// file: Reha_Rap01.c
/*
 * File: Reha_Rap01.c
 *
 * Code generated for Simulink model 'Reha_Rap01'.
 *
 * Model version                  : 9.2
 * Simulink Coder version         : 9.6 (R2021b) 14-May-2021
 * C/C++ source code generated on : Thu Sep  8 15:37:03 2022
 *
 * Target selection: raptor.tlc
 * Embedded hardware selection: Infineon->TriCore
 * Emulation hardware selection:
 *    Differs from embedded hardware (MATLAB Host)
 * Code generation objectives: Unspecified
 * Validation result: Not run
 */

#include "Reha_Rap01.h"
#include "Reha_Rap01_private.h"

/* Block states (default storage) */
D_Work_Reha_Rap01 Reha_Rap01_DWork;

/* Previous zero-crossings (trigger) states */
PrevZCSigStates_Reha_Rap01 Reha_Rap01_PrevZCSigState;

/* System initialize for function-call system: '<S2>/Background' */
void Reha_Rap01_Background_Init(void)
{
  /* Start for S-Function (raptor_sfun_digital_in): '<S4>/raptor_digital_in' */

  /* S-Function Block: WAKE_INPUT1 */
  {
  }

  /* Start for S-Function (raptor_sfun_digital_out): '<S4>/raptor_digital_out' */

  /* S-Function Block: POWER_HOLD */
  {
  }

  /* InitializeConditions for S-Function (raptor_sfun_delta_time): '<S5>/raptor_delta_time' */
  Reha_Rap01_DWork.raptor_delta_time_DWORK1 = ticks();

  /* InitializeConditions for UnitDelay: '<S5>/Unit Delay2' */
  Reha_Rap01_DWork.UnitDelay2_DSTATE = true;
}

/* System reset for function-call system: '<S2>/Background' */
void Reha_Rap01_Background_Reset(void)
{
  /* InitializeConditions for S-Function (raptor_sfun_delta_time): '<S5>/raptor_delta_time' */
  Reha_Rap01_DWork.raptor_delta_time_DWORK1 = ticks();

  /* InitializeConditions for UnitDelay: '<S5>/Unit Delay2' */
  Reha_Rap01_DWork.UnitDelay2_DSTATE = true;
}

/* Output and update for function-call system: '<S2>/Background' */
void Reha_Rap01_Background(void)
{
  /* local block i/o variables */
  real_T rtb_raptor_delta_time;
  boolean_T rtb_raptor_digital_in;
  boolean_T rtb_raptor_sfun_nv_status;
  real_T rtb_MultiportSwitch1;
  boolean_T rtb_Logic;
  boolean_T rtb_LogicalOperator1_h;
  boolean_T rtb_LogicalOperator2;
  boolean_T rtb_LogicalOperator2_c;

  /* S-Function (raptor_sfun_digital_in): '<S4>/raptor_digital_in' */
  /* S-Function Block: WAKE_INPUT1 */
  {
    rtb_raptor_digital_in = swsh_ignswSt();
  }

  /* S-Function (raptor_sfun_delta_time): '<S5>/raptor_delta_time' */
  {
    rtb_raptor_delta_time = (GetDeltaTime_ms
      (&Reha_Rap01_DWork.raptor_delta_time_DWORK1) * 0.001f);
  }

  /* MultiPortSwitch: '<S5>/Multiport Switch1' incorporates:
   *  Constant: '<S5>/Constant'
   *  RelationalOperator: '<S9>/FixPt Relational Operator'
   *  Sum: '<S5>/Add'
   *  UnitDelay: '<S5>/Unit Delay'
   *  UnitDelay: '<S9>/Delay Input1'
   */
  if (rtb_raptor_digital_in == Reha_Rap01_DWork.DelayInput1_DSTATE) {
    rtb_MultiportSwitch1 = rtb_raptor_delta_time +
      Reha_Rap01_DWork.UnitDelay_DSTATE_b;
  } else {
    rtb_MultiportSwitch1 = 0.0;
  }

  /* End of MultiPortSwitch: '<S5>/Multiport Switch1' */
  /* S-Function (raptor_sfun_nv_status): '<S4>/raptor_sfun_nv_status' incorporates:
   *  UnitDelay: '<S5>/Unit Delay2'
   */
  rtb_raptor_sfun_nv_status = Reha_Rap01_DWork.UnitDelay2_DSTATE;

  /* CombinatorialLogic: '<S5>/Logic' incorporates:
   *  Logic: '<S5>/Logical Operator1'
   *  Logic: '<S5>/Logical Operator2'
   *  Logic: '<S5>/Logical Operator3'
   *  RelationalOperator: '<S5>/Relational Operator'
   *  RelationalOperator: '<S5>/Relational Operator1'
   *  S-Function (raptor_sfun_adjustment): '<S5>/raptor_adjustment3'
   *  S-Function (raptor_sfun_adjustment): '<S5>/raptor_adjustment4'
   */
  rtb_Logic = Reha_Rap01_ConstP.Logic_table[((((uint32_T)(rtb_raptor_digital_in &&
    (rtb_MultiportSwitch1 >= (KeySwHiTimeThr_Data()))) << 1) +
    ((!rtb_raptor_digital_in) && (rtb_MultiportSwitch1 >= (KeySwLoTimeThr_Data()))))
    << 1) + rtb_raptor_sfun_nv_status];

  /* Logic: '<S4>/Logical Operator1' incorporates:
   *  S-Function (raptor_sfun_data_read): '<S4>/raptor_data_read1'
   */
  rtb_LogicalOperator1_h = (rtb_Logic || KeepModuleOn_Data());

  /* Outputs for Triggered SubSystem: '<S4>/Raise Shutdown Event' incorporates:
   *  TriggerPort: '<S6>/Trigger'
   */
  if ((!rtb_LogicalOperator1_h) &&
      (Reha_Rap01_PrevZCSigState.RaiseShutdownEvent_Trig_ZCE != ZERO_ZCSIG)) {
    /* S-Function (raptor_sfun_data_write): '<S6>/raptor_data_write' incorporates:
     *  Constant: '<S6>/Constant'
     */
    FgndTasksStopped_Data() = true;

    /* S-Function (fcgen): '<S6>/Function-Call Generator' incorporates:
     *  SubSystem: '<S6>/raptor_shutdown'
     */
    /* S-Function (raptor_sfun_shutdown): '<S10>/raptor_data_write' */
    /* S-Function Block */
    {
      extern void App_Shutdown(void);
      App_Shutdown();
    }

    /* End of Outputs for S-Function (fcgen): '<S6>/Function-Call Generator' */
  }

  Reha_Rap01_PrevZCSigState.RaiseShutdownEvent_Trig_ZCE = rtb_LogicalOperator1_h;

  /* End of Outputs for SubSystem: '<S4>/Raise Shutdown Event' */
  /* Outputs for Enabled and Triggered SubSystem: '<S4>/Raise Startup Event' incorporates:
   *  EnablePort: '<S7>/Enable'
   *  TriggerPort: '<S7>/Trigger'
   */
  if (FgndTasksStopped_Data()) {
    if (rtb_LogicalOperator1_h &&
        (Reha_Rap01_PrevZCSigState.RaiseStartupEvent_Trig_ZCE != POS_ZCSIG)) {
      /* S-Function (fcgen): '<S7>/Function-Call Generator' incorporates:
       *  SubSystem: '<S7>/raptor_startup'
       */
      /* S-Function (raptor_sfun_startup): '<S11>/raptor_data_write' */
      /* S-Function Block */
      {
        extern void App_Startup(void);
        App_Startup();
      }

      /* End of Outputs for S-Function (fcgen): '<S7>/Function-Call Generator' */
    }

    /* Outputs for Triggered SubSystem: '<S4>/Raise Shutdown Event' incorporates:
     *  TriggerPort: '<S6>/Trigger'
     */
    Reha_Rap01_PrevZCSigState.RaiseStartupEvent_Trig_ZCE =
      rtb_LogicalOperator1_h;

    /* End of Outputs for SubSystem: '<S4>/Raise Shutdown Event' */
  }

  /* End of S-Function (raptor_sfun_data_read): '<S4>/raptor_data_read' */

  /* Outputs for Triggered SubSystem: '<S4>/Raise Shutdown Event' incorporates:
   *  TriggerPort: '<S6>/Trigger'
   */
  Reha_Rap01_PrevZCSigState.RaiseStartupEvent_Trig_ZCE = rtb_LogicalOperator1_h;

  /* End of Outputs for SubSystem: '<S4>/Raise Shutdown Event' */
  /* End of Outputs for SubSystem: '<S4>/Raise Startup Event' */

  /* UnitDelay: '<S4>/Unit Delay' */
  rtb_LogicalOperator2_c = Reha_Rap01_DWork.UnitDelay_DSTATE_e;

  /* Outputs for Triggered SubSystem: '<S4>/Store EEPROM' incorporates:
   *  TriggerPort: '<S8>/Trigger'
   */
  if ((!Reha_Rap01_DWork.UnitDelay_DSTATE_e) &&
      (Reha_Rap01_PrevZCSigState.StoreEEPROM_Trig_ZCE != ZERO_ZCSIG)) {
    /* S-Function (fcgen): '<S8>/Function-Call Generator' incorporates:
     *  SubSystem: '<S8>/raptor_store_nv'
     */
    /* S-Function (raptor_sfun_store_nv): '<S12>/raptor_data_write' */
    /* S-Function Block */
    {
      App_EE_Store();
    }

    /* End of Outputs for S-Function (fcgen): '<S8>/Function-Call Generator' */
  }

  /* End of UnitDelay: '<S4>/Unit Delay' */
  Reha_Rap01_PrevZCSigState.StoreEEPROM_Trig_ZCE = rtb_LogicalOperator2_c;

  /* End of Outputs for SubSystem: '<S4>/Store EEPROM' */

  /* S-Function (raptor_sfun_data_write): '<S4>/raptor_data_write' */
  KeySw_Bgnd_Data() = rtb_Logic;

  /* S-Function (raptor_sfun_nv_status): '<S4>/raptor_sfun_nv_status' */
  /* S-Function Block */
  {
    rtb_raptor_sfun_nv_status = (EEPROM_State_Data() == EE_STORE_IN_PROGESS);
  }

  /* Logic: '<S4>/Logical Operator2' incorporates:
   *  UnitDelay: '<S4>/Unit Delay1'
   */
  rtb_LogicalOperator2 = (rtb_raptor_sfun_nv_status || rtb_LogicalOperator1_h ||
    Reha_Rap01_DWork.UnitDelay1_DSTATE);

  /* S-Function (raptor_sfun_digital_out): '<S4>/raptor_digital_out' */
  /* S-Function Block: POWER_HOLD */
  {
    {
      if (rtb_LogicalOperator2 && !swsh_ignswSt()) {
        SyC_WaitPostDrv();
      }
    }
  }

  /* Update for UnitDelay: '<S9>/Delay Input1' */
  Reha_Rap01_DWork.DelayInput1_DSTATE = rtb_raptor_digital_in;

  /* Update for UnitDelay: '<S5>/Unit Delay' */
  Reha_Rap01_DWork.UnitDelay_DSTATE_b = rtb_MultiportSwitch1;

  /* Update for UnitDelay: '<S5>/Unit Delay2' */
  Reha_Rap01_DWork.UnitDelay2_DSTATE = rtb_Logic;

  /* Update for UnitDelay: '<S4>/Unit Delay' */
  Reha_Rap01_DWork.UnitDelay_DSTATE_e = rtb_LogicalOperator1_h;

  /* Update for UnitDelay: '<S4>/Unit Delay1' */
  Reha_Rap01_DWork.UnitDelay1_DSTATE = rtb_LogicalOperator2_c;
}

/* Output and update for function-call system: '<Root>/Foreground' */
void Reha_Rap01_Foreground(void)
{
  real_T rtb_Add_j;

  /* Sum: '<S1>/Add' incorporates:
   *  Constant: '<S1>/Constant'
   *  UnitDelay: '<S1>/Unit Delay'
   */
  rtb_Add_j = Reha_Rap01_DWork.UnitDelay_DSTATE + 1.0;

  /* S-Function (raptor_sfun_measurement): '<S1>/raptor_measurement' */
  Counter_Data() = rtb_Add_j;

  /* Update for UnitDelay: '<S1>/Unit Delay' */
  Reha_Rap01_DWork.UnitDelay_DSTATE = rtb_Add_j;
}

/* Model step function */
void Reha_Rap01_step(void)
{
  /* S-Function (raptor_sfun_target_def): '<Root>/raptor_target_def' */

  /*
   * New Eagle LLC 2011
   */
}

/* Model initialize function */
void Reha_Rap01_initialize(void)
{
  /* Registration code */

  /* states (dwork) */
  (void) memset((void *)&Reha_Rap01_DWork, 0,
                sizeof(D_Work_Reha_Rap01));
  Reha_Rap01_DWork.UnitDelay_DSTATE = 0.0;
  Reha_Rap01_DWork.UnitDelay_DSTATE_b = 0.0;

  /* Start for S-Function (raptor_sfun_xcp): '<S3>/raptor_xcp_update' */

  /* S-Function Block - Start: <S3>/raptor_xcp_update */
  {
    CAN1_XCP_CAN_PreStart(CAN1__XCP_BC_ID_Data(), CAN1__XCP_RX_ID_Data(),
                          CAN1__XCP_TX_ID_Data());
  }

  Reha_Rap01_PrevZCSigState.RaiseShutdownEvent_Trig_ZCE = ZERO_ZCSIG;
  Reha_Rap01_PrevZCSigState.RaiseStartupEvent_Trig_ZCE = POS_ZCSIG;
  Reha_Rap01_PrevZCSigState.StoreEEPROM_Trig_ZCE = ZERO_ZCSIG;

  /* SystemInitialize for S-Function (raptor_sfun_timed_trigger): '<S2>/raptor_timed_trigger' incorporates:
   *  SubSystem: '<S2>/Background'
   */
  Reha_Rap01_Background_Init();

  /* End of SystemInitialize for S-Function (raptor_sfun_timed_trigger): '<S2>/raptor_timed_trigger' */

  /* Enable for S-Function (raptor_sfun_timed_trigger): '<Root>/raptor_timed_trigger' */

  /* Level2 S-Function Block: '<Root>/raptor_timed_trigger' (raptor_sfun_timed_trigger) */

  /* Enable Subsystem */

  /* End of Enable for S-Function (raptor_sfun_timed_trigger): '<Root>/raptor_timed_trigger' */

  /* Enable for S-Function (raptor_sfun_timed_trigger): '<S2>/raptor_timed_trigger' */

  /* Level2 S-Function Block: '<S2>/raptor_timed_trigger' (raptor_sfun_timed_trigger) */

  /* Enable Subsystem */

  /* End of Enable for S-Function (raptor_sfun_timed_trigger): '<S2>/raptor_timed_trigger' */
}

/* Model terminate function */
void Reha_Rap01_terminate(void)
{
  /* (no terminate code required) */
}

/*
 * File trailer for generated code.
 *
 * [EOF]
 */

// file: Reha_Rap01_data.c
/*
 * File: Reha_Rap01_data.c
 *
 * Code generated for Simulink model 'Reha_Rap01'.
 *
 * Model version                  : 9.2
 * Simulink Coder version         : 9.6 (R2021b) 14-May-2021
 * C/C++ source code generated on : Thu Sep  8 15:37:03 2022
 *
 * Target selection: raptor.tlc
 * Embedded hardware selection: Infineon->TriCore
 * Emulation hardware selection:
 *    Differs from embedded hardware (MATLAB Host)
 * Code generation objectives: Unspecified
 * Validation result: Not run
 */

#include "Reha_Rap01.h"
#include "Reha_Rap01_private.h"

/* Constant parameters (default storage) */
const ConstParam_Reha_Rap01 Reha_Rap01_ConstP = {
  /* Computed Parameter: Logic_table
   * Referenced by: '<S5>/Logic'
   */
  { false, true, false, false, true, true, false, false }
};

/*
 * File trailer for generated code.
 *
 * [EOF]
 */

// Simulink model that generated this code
simulink model "Reha_Rap01"  (R2021b)
settings: Solver=FixedStepDiscrete  StartTime=0.0  StopTime=10.0  FixedStep=0.005  RelTol=1e-3  EnableMultiTasking=on
PreLoadFcn:
  | try, model_open; catch, disp('Error occurred while executing model pre-load callback: model_open.m'); disp('Please assure that the MATLAB working directory is set to the model directory before opening.'); end
InitFcn:
  | try, model_open; catch, end
undefined symbols (not defined in the file): ECM, raptor_get_safe_string, raptor_xcp_function
libraries: Raptor_lib x22, simulink x4

== system Reha_Rap01 ==
  Foreground : Subsystem  TreatAsAtomicUnit=on
  Power Up_Down : Subsystem  mask{group='Diagnostics | Power Up_Down'}
  raptor_can_def : Raptor_lib/CAN/raptor_can_def  canBus='CAN1'  resourceValues=(None)|CAN1|CAN2  resource=CAN1  baudRateValues=250k  baudRate=250k  enable_baud_rate_config='RAPTOR MASK DEFAULT'  sim_func_name='RAPTOR MASK DEFAULT'  createButton=[]  txQueueSize=16  rxQueueSize=16
  raptor_target_def : Raptor_lib/Configuration/raptor_target_def  targetValues=HCM-5534-50-1203|HCM-5534-90-1201|HCM-5534-90-1302|HCM-5604-36-1303|HCM-ARM4-070-1401|DISP-IMX286-036-1402|DISP-IMX286-024-1204|DISP-IMX286-012-1402  target=ECM-1793-196-1503  simpack=0  simulator=0  heap=4*1024  stack=2*1024  fgndStack=3*1024  bgndStack=2*1024  idleStack=1024  intStack=1536  sdStack=1024  appStack=1024  ecuaddr=11  uds_server_addr_ext=0  uds_server_addr=hex2dec('600')  uds_client_addr=hex2dec('650')  callocValues=Constant (FLASH)|NonVolatile (EEPROM)  calloc=NonVolatile (EEPROM)  compilerValues=HighTec v3.4.5.11  compiler=HighTec v3.4.5.11  setFileName=0  exeName=[raptor_get_safe_string(bdroot) '_']  addBuildNum=1  minVerChars=3  extraOutput=0  buildLocationValues=Raptor Default|Model Directory|User Defined  buildLocation=Raptor Default  exeLocation=''  exeFileButton=[]  a2lLocation=''  a2lFileButton=[]  rpgLocation=''  rpgFileButton=[]
  raptor_timed_trigger : Raptor_lib/Triggers/raptor_timed_trigger  triggerValues=[]  trigger=Foreground  inherited=0  alwaysEnabled=1  triggerPriority=0  triggerName=ooqlV
  raptor_xcp_def : Raptor_lib/Configuration/raptor_xcp_def  canBus='CAN1'  bcID=hex2dec('100')  bcID_TypeValues=Standard|Extended  bcID_Type=Standard  rxID=hex2dec('200')  rxID_TypeValues=Standard|Extended  rxID_Type=Standard  txID=hex2dec('300')  txID_TypeValues=Standard|Extended  txID_Type=Standard  daqRates=[10 100]  numODTs=20  genCANAPE=0  genVISION=0  securityValues=Standard|None|Custom User Defined|MH_SB_4  security=Standard  dllName=raptor_XCPSecurity.dll  accessValues=4|3|2|1  access=1  bcStorageValues=[]  bcStorage=Calibration  txStorageValues=[]  txStorage=Calibration  rxStorageValues=[]  rxStorage=Calibration
  wires:
  raptor_timed_trigger/1 -> Foreground/Trigger

== system Reha_Rap01/Foreground ==
  function : TriggerPort  TriggerType=function-call  VariantControl=Variant
  Add : Sum
  Constant : Constant
  Unit Delay : UnitDelay  SampleTime=-1  HasFrameUpgradeWarning=on
  raptor_measurement : Raptor_lib/Data Storage/raptor_measurement  paramName='Counter'  nameSource=Parameter  calDispType=Number  calEnum={'False', 'True'}  calGain=1.0  calOffset=0.0  calMax=inf  calMin=-inf  calFormat='-1'  calUnit=''  calHelp=''  calAccess=4  calFunction=raptor_xcp_function(gcb)  calVisible=on
  wires:
  Constant/1 -> Add/1
  Add/1 -> raptor_measurement/1, Unit Delay/1
  Unit Delay/1 -> Add/2

== system Reha_Rap01/Power Up_Down ==
  Background : Subsystem
  raptor_timed_trigger : Raptor_lib/Triggers/raptor_timed_trigger  triggerValues=Foreground|Foregroundx2|Foregroundx5|Foregroundx10|Foregroundx20|Background|Backgroundx2|Backgroundx5|Backgroundx10|Backgroundx20|Second|Minute  trigger=Background  inherited=0  alwaysEnabled=1  triggerPriority=50  triggerName=BGND_G6Wyo
  wires:
  raptor_timed_trigger/1 -> Background/Trigger

== system Reha_Rap01/Power Up_Down/Background ==
  note: Notes :
      | - Calling the shutdown task stops the foreground tasks. However, background tasks continue, so the reading of key switch must be in this subsystem to allow the module
      | to resume operation (by calling the startup task) if keyswitch is turned back on before the module actually turns off.
      | - The Startup Event is automatically called when the module is powered on after being completely off. The FgndTasksStopped data store prevents the Startup Event from being called twice in this scenario.
  f : TriggerPort  TriggerType=function-call  VariantControl=Variant  ZeroCross=off
  Debounce : Subsystem
  Logical Operator1 : Logic  Operator=OR  OutDataTypeStr=boolean
  Logical Operator2 : Logic  Operator=OR  Inputs=3  OutDataTypeStr=boolean
  Raise Shutdown Event : Subsystem  TreatAsAtomicUnit=on
  Raise Startup Event : Subsystem  TreatAsAtomicUnit=on
  Store EEPROM : Subsystem  TreatAsAtomicUnit=on
  Unit Delay : UnitDelay  SampleTime=-1  HasFrameUpgradeWarning=on
  Unit Delay1 : UnitDelay  SampleTime=-1  HasFrameUpgradeWarning=on
  raptor_data_def : Raptor_lib/Data Storage/raptor_data_def  dataName='KeySw_Bgnd'  initValue=0  dataType=boolean  storage=Volatile (RAM)  calVisible=on  calType=Measurement  calDispType=Number  calEnum={'False', 'True'}  calGain=1.0  calOffset=0  calMin=-Inf  calMax=Inf  calFormat='-1'  calUnit='Bool'  calHelp='Key switch reading from background task'  calAccess=1  calFunction=group  calDispHeaders=off  calColHeaders={'Col1' 'Col2' 'Col3'}  calRowHeaders={'Row1' 'Row2' 'Row3'}
  raptor_data_def1 : Raptor_lib/Data Storage/raptor_data_def  dataName='KeepModuleOn'  initValue=0  dataType=boolean  storage=Volatile (RAM)  calVisible=on  calType=Measurement  calDispType=Number  calEnum={'False', 'True'}  calGain=1.0  calOffset=0  calMin=-Inf  calMax=Inf  calFormat='-1'  calUnit='Bool'  calHelp='Boolean indicating module to be kept on'  calAccess=1  calFunction=group  calDispHeaders=off  calColHeaders={'Col1' 'Col2' 'Col3'}  calRowHeaders={'Row1' 'Row2' 'Row3'}
  raptor_data_read : Raptor_lib/Data Storage/raptor_data_read  dataName='FgndTasksStopped'  dataShape=Scalar  idxSource=Input  idxRow=1  idxCol=1
  raptor_data_read1 : Raptor_lib/Data Storage/raptor_data_read  dataName='KeepModuleOn'  dataShape=Scalar  idxSource=Input  idxRow=1  idxCol=1
  raptor_data_write : Raptor_lib/Data Storage/raptor_data_write  dataName='KeySw_Bgnd'  dataShape=Scalar  idxSource=Input Port  idxRow=1  idxCol=1
  raptor_digital_in : Raptor_lib/Input & Output/raptor_digital_in  resourceValues=(None)|WAKE_INPUT1|INPUT33|INPUT34|INPUT35|INPUT36|INPUT37|INPUT38|INPUT39|INPUT40  resource=WAKE_INPUT1  pullUDValues=2.9k PD  pullUD=2.9k PD  upperThres=1.980  lowerThres=1.320
  raptor_digital_out : Raptor_lib/Input & Output/raptor_digital_out  resourceValues=OUTPUT9|OUTPUT21|OUTPUT22|OUTPUT23|OUTPUT24|(None)|OUTPUT1|OUTPUT2|OUTPUT3|OUTPUT4|OUTPUT5|OUTPUT6|OUTPUT7|OUTPUT8|OUTPUT10|OUTPUT11|OUTPUT25|OUTPUT26|OUTPUT27|OUTPUT28|OUTPUT29|OUTPUT30|OUTPUT31|OUTPUT32|OUTPUT33|OUTPUT34|OUTPUT35|OUTPUT36|OUTPUT37|OUTPUT38|OUTPUT39|OUTPUT40|OUTPUT41|OUTPUT42|OUTPUT43|OUTPUT44|OUTPUT45|OUTPUT46|OUTPUT47|OUTPUT48|POWER_HOLD  resource=POWER_HOLD  driverTypeValues=(None)  driverType=(None)
  raptor_sfun_nv_status : Raptor_lib/Data Storage/raptor_sfun_nv_status  showStatus=Store In Progess
  wires:
  raptor_data_read/1 -> Raise Startup Event/Enable
  raptor_digital_in/1 -> Debounce/1(In)
  Logical Operator2/1 -> raptor_digital_out/1
  Unit Delay/1 -> Store EEPROM/Trigger, Unit Delay1/1
  Logical Operator1/1 -> Logical Operator2/2, Raise Startup Event/Trigger, Raise Shutdown Event/Trigger, Unit Delay/1
  Unit Delay1/1 -> Logical Operator2/3
  raptor_sfun_nv_status/1 -> Logical Operator2/1
  raptor_data_read1/1 -> Logical Operator1/2
  Debounce/1(Out) -> raptor_data_write/1, Logical Operator1/1

== system Reha_Rap01/Power Up_Down/Background/Debounce ==
  note: Set / Reset
  In : Inport
  Add : Sum
  Constant : Constant  Value=double(0)
  Detect Change : simulink/Logic and Bit Operations/Detect Change  vinit=0  OutDataTypeStr=boolean
  Logic : CombinatorialLogic  TruthTable=[0;1;0;0;1;1;0;0]
  Logical Operator1 : Logic  AllPortsSameDT=off  OutDataTypeStr=boolean
  Logical Operator2 : Logic  AllPortsSameDT=off  OutDataTypeStr=boolean
  Logical Operator3 : Logic  Operator=NOT  Inputs=1  AllPortsSameDT=off  OutDataTypeStr=boolean
  Multiport Switch1 : MultiPortSwitch  DataPortOrder=Zero-based contiguous  Inputs=2  zeroidx=on
  Mux1 : Mux  Inputs=3
  Relational Operator : RelationalOperator  OutDataTypeStr=boolean  RndMeth=Nearest
  Relational Operator1 : RelationalOperator  OutDataTypeStr=boolean  RndMeth=Nearest
  Unit Delay : UnitDelay  SampleTime=-1  HasFrameUpgradeWarning=on
  Unit Delay2 : UnitDelay  InitialCondition=1  SampleTime=-1  HasFrameUpgradeWarning=on
  raptor_adjustment3 : Raptor_lib/Data Storage/raptor_adjustment  paramName='KeySwHiTimeThr'  nameSource=Parameter  initValue=0.2  dataType=double  storage=Calibration  calDispType=Number  calEnum={'Active Low', 'Active High'}  calGain=1  calOffset=0  calMax=inf  calMin=-inf  calFormat='-1'  calUnit='sec'  calHelp='State high time threshold'  calAccess=1  calFunction=group  calDispHeaders=off  calColHeaders={'Col1' 'Col2' 'Col3'}  calRowHeaders={'Row1' 'Row2' 'Row3'}
  raptor_adjustment4 : Raptor_lib/Data Storage/raptor_adjustment  paramName='KeySwLoTimeThr'  nameSource=Parameter  initValue=0.2  dataType=double  storage=Calibration  calDispType=Number  calEnum={'Active Low', 'Active High'}  calGain=1  calOffset=0  calMax=inf  calMin=-inf  calFormat='-1'  calUnit='sec'  calHelp='State low time threshold'  calAccess=1  calFunction=group  calDispHeaders=off  calColHeaders={'Col1' 'Col2' 'Col3'}  calRowHeaders={'Row1' 'Row2' 'Row3'}
  raptor_delta_time : Raptor_lib/Triggers/raptor_delta_time  unit=seconds
  Out : Outport  VectorParamsAs1DForOutWhenUnconnected=off
  wires:
  Detect Change/1 -> Multiport Switch1/1
  Logical Operator3/1 -> Logical Operator2/1
  Relational Operator/1 -> Logical Operator1/2
  Logical Operator2/1 -> Mux1/2
  Logical Operator1/1 -> Mux1/1
  Mux1/1 -> Logic/1
  Unit Delay2/1 -> Mux1/3
  In/1 -> Detect Change/1, Logical Operator1/1, Logical Operator3/1
  Multiport Switch1/1 -> Unit Delay/1, Relational Operator/1, Relational Operator1/1
  Add/1 -> Multiport Switch1/2
  Constant/1 -> Multiport Switch1/3
  Relational Operator1/1 -> Logical Operator2/2
  Logic/1 -> Unit Delay2/1, Out/1
  Unit Delay/1 -> Add/2
  raptor_delta_time/1 -> Add/1
  raptor_adjustment4/1 -> Relational Operator1/2
  raptor_adjustment3/1 -> Relational Operator/2

== system Reha_Rap01/Power Up_Down/Background/Raise Shutdown Event ==
  Trigger : TriggerPort  TriggerType=falling  VariantControl=Variant
  Constant : Constant  Value=boolean(1)
  Function-Call Generator : simulink/Ports & Subsystems/Function-Call Generator  sample_time=-1  numberOfIterations=1  DisallowWideOutput=off
  raptor_data_def : Raptor_lib/Data Storage/raptor_data_def  dataName='FgndTasksStopped'  initValue=0  dataType=boolean  storage=Volatile (RAM)  calVisible=on  calType=Measurement  calDispType=Number  calEnum={'False', 'True'}  calGain=1.0  calOffset=0  calMin=-Inf  calMax=Inf  calFormat='-1'  calUnit='Bool'  calHelp='Boolean indicating foreground tasks stopped'  calAccess=1  calFunction=group  calDispHeaders=off  calColHeaders={'Col1' 'Col2' 'Col3'}  calRowHeaders={'Row1' 'Row2' 'Row3'}
  raptor_data_write : Raptor_lib/Data Storage/raptor_data_write  dataName='FgndTasksStopped'  dataShape=Scalar  idxSource=Input Port  idxRow=1  idxCol=1
  raptor_shutdown : Raptor_lib/Triggers/raptor_shutdown  null=0
  wires:
  Constant/1 -> raptor_data_write/1
  Function-Call Generator/1 -> raptor_shutdown/Trigger

== system Reha_Rap01/Power Up_Down/Background/Raise Startup Event ==
  Enable : EnablePort
  Trigger : TriggerPort  VariantControl=Variant
  Function-Call Generator : simulink/Ports & Subsystems/Function-Call Generator  sample_time=-1  numberOfIterations=1  DisallowWideOutput=off
  raptor_startup : Raptor_lib/Triggers/raptor_startup  null=0
  wires:
  Function-Call Generator/1 -> raptor_startup/Trigger

== system Reha_Rap01/Power Up_Down/Background/Store EEPROM ==
  Trigger : TriggerPort  TriggerType=falling  VariantControl=Variant
  Function-Call Generator : simulink/Ports & Subsystems/Function-Call Generator  sample_time=-1  numberOfIterations=1  DisallowWideOutput=off
  raptor_store_nv : Raptor_lib/Data Storage/raptor_store_nv  null=0
  wires:
  Function-Call Generator/1 -> raptor_store_nv/Trigger
